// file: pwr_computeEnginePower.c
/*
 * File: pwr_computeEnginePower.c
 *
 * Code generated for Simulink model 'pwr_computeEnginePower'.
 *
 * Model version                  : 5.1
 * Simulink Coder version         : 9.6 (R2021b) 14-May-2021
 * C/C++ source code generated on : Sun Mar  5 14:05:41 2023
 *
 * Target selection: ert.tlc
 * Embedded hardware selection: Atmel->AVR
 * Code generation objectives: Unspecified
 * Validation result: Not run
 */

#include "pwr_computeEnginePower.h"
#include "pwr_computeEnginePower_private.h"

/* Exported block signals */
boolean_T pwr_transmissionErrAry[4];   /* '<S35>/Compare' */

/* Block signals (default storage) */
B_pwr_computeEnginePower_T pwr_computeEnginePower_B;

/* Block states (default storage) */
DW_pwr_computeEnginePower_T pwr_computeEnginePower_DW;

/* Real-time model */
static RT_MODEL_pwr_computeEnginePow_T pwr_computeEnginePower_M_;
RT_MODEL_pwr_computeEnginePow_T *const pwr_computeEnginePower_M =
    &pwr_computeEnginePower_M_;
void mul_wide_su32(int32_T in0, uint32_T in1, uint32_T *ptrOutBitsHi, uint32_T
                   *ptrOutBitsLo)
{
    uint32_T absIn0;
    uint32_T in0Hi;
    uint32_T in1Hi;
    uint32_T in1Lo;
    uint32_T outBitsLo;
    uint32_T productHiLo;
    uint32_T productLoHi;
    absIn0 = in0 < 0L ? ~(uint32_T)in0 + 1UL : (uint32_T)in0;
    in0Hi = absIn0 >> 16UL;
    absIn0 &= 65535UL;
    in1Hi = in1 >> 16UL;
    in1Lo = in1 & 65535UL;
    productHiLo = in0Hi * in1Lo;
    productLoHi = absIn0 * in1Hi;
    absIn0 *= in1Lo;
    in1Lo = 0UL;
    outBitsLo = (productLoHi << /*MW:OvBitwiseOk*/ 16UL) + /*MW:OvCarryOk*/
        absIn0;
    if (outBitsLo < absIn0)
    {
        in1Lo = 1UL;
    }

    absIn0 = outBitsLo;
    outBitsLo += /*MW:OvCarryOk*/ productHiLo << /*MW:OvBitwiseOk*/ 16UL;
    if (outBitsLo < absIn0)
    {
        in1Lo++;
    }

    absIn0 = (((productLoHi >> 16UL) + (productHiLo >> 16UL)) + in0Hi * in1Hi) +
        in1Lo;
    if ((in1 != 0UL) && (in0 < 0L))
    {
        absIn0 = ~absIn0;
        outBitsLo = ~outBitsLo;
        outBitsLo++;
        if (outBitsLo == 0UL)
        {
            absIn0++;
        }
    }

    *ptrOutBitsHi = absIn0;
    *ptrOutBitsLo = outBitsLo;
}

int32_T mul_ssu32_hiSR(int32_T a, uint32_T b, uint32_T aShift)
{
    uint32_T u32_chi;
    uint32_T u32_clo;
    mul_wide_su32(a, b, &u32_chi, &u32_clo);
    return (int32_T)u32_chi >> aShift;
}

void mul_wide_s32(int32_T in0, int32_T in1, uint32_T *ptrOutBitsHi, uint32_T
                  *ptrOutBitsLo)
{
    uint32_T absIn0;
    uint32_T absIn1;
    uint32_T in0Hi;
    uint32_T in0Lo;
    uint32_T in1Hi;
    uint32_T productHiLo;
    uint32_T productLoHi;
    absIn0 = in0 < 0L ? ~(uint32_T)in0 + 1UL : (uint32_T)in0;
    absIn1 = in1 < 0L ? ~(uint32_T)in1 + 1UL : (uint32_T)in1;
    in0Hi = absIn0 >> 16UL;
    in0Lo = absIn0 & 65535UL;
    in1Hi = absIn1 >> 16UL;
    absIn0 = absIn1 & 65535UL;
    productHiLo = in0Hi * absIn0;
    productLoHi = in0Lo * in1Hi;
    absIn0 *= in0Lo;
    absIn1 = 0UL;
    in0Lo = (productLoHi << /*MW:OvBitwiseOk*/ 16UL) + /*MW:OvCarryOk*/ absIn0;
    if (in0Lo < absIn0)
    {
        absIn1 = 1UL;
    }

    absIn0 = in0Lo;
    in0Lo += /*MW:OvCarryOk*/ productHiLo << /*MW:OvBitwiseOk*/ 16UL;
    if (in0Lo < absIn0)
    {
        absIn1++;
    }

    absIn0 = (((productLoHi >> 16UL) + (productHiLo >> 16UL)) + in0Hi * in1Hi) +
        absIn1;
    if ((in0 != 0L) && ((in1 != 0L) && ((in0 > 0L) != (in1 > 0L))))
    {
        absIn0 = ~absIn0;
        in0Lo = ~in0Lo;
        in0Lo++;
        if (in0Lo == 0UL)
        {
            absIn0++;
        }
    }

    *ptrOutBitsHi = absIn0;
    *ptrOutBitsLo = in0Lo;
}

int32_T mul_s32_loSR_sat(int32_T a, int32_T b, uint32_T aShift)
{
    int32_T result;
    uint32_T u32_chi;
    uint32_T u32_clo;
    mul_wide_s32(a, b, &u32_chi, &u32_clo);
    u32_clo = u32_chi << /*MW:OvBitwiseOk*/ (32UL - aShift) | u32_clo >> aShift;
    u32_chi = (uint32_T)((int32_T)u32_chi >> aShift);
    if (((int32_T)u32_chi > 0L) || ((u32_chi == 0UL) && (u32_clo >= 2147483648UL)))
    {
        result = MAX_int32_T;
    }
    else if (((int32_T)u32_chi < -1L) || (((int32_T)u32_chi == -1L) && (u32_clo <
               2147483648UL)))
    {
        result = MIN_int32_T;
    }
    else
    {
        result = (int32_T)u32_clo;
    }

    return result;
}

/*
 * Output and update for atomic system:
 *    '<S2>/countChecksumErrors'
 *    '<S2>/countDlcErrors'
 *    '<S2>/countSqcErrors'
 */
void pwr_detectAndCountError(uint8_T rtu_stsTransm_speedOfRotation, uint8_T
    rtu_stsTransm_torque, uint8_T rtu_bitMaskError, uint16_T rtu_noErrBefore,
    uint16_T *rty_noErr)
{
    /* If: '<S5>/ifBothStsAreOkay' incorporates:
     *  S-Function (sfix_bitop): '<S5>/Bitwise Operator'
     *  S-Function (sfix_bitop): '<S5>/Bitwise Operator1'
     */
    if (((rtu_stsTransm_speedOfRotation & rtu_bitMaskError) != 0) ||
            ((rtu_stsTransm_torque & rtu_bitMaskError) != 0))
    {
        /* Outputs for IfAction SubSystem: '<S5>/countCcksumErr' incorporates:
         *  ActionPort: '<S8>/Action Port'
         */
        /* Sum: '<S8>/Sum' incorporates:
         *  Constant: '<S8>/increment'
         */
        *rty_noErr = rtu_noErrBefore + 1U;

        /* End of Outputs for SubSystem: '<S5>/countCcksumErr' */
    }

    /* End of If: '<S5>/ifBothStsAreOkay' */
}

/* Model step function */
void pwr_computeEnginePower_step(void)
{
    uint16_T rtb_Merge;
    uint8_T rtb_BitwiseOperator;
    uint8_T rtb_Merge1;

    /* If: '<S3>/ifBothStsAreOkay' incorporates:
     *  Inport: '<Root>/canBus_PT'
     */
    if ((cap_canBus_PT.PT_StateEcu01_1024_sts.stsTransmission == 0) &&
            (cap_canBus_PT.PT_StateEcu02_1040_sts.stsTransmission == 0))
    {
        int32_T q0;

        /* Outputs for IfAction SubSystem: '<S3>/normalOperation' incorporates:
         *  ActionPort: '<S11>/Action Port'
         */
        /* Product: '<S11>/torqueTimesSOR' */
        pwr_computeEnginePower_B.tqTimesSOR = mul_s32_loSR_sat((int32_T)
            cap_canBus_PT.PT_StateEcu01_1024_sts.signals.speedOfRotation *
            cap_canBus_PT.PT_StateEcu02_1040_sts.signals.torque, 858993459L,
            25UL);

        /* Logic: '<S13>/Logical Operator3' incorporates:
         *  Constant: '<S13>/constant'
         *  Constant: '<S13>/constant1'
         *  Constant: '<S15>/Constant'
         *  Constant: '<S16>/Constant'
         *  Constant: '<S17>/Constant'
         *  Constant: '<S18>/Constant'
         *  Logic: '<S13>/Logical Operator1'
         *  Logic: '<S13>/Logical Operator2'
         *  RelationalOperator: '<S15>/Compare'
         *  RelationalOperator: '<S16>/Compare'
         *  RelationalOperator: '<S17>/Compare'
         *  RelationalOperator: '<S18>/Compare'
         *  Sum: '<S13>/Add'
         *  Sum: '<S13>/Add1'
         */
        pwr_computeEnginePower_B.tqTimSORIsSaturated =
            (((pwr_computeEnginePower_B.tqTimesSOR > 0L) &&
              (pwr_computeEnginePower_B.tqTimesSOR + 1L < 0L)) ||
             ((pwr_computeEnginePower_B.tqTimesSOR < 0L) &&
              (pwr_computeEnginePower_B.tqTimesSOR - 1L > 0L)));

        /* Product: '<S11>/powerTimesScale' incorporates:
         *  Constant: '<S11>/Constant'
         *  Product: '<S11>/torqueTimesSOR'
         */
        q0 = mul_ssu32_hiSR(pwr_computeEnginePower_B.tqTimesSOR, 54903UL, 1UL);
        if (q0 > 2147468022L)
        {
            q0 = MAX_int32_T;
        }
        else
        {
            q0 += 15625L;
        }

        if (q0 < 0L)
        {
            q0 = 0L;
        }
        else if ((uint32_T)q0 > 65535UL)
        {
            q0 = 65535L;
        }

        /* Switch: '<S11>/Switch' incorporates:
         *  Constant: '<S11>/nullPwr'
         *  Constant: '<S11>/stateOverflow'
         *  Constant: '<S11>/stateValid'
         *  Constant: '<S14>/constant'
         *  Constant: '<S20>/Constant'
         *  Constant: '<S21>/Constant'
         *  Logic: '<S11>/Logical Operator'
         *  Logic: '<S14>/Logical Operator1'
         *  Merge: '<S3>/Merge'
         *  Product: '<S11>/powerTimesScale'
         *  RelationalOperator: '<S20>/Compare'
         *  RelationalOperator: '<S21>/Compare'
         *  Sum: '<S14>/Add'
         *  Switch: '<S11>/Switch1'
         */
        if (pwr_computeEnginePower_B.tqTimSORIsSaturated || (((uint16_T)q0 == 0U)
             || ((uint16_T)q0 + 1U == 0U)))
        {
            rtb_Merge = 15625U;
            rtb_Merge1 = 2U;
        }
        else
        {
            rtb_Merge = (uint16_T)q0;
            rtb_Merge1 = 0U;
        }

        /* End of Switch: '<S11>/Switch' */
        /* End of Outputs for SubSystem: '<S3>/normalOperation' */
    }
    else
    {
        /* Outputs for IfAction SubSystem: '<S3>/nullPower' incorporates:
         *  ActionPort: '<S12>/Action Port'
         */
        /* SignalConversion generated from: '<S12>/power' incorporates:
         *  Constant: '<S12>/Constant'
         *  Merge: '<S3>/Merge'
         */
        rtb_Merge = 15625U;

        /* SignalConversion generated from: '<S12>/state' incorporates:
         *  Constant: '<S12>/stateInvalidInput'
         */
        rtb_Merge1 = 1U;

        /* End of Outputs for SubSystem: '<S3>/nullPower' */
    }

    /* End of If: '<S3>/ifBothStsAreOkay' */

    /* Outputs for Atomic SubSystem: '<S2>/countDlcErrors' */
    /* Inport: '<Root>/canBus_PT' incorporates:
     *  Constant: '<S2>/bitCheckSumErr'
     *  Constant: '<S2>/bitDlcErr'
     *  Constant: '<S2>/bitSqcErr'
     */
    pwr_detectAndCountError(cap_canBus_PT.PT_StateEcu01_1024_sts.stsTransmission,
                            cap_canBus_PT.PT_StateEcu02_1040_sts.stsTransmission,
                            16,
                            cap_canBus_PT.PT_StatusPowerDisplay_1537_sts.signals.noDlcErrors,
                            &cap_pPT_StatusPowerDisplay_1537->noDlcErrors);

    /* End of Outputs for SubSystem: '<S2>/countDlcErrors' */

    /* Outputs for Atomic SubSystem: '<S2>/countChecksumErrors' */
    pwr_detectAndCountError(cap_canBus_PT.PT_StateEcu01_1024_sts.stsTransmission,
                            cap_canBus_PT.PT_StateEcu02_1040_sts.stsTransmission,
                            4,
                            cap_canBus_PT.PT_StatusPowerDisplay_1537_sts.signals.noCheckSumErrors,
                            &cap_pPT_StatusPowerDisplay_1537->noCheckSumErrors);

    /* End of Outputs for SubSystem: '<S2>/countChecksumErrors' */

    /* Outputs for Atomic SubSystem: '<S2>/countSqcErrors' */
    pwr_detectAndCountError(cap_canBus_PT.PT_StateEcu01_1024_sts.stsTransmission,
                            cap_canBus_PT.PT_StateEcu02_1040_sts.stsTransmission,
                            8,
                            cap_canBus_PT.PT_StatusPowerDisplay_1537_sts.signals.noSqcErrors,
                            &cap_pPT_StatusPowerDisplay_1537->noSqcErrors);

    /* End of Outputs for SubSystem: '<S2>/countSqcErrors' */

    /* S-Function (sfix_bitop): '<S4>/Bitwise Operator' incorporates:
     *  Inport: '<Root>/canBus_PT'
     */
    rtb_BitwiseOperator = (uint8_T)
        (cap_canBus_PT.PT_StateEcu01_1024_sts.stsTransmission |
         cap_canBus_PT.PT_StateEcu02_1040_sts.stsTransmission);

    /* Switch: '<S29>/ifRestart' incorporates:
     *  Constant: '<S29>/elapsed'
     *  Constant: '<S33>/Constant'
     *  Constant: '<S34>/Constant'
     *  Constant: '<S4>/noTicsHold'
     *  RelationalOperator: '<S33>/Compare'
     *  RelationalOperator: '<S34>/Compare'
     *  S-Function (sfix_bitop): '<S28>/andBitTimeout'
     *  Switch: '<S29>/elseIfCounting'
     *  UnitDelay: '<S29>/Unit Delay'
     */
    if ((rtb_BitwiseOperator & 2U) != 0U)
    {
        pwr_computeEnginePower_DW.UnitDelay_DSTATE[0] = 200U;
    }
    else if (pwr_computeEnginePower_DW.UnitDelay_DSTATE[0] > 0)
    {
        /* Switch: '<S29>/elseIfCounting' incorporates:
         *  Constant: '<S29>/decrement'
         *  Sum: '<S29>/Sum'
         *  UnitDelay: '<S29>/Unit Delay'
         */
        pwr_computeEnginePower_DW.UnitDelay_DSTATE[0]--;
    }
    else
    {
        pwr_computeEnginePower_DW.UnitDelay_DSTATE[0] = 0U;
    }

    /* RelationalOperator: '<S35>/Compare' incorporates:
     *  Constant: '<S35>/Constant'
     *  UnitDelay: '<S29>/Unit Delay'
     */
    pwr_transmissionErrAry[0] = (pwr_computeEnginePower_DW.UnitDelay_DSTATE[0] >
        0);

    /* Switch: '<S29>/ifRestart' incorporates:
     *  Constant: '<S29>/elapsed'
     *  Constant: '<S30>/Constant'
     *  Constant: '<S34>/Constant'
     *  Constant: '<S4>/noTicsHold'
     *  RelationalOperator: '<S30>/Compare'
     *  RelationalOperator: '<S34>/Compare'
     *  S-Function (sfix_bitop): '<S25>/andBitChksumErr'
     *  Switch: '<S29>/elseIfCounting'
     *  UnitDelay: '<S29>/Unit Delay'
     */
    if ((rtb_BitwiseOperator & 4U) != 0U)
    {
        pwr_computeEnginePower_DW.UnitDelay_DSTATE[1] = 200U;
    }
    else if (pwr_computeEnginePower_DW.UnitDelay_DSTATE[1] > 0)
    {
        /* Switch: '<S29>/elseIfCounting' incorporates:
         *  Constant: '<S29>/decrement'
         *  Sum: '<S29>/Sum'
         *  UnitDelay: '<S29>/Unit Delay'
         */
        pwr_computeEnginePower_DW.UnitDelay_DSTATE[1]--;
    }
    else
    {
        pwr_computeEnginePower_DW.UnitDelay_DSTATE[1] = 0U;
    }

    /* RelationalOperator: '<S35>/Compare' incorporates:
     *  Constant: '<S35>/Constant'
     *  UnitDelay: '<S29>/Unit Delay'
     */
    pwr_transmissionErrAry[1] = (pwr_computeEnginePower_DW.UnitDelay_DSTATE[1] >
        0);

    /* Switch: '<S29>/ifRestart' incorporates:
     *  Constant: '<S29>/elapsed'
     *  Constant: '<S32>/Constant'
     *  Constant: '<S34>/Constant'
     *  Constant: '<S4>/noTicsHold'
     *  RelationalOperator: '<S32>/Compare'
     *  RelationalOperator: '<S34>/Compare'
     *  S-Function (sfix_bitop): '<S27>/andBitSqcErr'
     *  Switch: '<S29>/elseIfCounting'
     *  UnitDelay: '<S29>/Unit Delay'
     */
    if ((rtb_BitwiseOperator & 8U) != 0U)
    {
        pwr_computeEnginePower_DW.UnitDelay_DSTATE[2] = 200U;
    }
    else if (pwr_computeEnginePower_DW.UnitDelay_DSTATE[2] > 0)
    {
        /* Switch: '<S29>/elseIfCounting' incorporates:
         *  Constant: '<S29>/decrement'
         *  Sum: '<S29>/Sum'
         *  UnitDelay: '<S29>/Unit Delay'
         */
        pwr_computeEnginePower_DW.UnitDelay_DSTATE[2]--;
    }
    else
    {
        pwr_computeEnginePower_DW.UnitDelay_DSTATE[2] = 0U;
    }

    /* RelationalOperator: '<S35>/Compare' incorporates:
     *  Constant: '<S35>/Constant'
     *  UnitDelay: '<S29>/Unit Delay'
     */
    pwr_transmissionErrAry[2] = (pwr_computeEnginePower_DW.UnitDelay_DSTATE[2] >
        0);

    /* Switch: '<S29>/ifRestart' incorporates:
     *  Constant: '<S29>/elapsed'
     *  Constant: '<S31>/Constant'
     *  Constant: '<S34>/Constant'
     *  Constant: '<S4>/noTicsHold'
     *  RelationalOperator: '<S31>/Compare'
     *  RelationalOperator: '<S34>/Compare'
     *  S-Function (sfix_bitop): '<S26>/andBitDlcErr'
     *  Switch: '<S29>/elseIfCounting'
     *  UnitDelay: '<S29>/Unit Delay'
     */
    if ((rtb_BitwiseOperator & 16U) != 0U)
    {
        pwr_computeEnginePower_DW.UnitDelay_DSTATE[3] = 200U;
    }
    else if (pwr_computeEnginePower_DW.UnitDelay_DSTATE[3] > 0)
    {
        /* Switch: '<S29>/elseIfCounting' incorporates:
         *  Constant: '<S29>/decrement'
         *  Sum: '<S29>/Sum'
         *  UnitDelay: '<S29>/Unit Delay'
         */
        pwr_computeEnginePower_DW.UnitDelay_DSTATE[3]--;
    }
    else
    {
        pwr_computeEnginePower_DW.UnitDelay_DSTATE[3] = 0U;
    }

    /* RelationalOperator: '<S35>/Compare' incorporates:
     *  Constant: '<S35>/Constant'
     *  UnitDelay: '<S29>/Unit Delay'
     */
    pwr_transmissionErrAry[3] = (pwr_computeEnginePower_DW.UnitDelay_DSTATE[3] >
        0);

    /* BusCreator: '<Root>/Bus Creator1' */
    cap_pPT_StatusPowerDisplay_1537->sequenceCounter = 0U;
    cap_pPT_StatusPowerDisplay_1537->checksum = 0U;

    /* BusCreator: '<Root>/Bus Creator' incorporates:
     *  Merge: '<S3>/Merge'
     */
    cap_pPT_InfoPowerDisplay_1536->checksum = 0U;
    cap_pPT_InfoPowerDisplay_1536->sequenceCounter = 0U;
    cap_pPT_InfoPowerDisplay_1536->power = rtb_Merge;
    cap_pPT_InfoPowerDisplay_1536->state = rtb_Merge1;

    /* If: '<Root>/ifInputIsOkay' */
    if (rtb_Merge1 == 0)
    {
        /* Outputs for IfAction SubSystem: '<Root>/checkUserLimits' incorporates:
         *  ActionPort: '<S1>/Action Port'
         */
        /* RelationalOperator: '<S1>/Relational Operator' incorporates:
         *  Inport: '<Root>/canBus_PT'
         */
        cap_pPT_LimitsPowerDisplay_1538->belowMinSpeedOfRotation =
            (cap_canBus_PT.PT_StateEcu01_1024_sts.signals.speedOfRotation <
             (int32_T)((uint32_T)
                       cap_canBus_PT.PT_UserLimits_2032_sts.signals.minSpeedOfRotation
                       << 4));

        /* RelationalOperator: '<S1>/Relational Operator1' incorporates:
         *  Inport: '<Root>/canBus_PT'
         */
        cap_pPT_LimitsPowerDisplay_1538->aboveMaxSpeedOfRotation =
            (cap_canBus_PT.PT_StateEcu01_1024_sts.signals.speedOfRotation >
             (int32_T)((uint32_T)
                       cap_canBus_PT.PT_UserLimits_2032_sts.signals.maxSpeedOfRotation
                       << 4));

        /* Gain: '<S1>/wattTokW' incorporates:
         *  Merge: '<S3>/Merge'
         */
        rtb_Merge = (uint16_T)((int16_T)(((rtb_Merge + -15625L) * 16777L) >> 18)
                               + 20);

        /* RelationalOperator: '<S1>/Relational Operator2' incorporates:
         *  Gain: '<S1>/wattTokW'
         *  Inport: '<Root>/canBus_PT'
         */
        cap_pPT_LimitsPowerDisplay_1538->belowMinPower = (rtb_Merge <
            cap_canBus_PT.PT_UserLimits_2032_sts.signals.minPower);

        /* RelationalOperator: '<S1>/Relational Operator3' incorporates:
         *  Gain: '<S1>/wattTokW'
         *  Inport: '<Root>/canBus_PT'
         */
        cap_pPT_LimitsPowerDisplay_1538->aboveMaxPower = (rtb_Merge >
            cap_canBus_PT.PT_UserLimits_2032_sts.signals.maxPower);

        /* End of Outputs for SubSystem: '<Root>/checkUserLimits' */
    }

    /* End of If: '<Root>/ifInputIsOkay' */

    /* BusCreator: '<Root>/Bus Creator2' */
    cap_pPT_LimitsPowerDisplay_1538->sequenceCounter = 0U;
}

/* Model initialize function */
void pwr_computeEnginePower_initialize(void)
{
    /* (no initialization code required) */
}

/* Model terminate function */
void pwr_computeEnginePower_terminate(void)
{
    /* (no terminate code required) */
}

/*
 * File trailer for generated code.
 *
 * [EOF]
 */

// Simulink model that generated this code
simulink model "pwr_computeEnginePower"  (R2021b)
settings: Solver=FixedStepDiscrete  StartTime=0.0  StopTime=10.0  RelTol=1e-3
libraries: simulink x27

== system pwr_computeEnginePower ==
  note: The comparison of actual values of speed of rotation
      |  and power with the user specified limits is done only
      | if the received frames are valid. This information is
      | derived from the status of the computed power signal
  note: Checksum and sequence counter are not
      | computed by the APSW but by the code
      | integration layer (the upper CAN stack layer).
      | Unfortunately forces the use of bus objects
      | setting all signals of th bus, not only of
      | the required. We write dummy values here,
      | which will be overwritten by the CAN stack
  canBus_PT : Inport  OutDataTypeStr=Bus: cap_canBus_PT_t  BusOutputAsStruct=on
  Bus Creator : BusCreator  Inputs=4  OutDataTypeStr=Bus: cap_PT_InfoPowerDisplay_1536_t  NonVirtualBus=on
  Bus Creator1 : BusCreator  Inputs=5  OutDataTypeStr=Bus: cap_PT_StatusPowerDisplay_1537_t  NonVirtualBus=on
  Bus Creator2 : BusCreator  Inputs=5  OutDataTypeStr=Bus: cap_PT_LimitsPowerDisplay_1538_t  NonVirtualBus=on
  Bus Selector : BusSelector  OutputSignals=PT_StateEcu01_1024_sts.signals.speedOfRotation,PT_StateEcu01_1024_sts.stsTransmission,PT_StateEcu02_1040_sts.signals.torque,PT_StateEcu02_1040_sts.stsTransmission,PT_UserLimits_2032_sts.signals.minSpeedOfRotation,PT_UserLimits_2032_sts.signals.maxSpeedOfRotation,PT_UserLimits_2032_sts.signals.minPower,PT_UserLimits_2032_sts.signals.maxPower,PT_UserLimits_2032_sts.stsTransmission,PT_StatusPowerDisplay_1537_sts.signals.noDlcErrors,PT_StatusPowerDisplay_1537_sts.signals.noCheckSumErrors,PT_StatusPowerDisplay_1537_sts.signals.noSqcErrors
  Ground_{1,8..10,15} (5 alike) : Ground
  Terminator_8 : Terminator
  checkUserLimits : Subsystem  TreatAsAtomicUnit=on  RTWFcnName=pwr_detectAndCountError
  cntTransmissionErrs : Subsystem
  ifInputIsOkay : If  IfExpression=u1 == 0  ShowElse=off
  powerComputation : Subsystem
  transmissionErrs : Subsystem
  InfoPowerDisplay : Outport  OutDataTypeStr=Bus: cap_PT_InfoPowerDisplay_1536_t
  StatusPowerDisplay : Outport  Port=2  OutDataTypeStr=Bus: cap_PT_StatusPowerDisplay_1537_t
  LimitsPowerDisplay : Outport  Port=3  OutDataTypeStr=Bus: cap_PT_LimitsPowerDisplay_1538_t
  pwr_transmissionErrAry : Outport  Port=4
  wires:
  Bus Creator1/1 -> StatusPowerDisplay/1  "PT_StatusPowerDisplay_1537"
  Ground_15/1 -> Bus Creator/2  "sequenceCounter"
  Bus Selector/8 -> checkUserLimits/6(maxPwr)  "<maxPower>"
  Bus Selector/10 -> cntTransmissionErrs/3(noDlcErrBefore)  "<noDlcErrors>"
  Bus Selector/9 -> Terminator_8/1  "<stsTransmission>"
  Bus Selector/7 -> checkUserLimits/5(minPwr)  "<minPower>"
  powerComputation/1(power) -> Bus Creator/3, checkUserLimits/4(power)  "power"
  canBus_PT/1 -> Bus Selector/1  "canBus_PT"
  Bus Selector/6 -> checkUserLimits/3(maxSOR)  "<maxSpeedOfRotation>"
  powerComputation/2(state) -> Bus Creator/4, ifInputIsOkay/1  "state"
  cntTransmissionErrs/2(noChksumErrs) -> Bus Creator1/2
  ifInputIsOkay/1 -> checkUserLimits/Action
  Bus Selector/11 -> cntTransmissionErrs/4(noChksumErrBefore)  "<noCheckSumErrors>"
  Bus Selector/5 -> checkUserLimits/2(minSOR)  "<minSpeedOfRotation>"
  transmissionErrs/1(errVecHold) -> pwr_transmissionErrAry/1  "pwr_transmissionErrAry"
  Ground_1/1 -> Bus Creator/1  "checksum"
  checkUserLimits/4(aboveMaxPower) -> Bus Creator2/5  "aboveMaxPower"
  Bus Creator2/1 -> LimitsPowerDisplay/1  "PT_LimitsPowerDisplay_1538"
  cntTransmissionErrs/3(noSqcErrs) -> Bus Creator1/3
  Bus Selector/4 -> powerComputation/4(stsTransm_torque), cntTransmissionErrs/2(stsTransm_torque1), transmissionErrs/2(stsTransm_torque)  "<stsTransmission>"
  checkUserLimits/3(belowMinPower) -> Bus Creator2/4  "belowMinPower"
  Ground_9/1 -> Bus Creator1/5  "checksum"
  Bus Selector/1 -> powerComputation/1(speedOfRotation), checkUserLimits/1(speedOfRotation)  "<speedOfRotation>"
  checkUserLimits/2(aboveMaxSpeedOfRotation) -> Bus Creator2/3  "aboveMaxSpeedOfRotation"
  Bus Selector/3 -> powerComputation/3(torque)  "<torque>"
  cntTransmissionErrs/1(noDlcErrs) -> Bus Creator1/1
  Bus Selector/12 -> cntTransmissionErrs/5(noSqcErrBefore)  "<noSqcErrors>"
  Bus Selector/2 -> powerComputation/2(stsTransm_speedOfRotation), cntTransmissionErrs/1(stsTransm_speedOfRotation), transmissionErrs/1(stsTransm_speedOfRotation)  "<stsTransmission>"
  checkUserLimits/1(belowMinSpeedOfRotation) -> Bus Creator2/2  "belowMinSpeedOfRotation"
  Bus Creator/1 -> InfoPowerDisplay/1  "PT_InfoPowerDisplay_1536"
  Ground_8/1 -> Bus Creator1/4  "sequenceCounter"
  Ground_10/1 -> Bus Creator2/1  "sequenceCounter"

== system pwr_computeEnginePower/checkUserLimits ==
  note: The input signals power limit
      | have the unit kW, whereas all other
      | power computation is done in W.
      | This is not part of the Embedded
      | Coder's scaling information and is
      | hence not considered by the code
      | generation. We need to perform
      | this kind of rescaling by an explicit
      | multiplication operation
  note: The rescaling required to implement
      | the comparisons introduce rounding
      | off errors, which make the limits check
      | not perfectly hit the boundaries. This
      | holds for SOR and power
  speedOfRotation : Inport
  minSOR : Inport  Port=2
  maxSOR : Inport  Port=3
  power : Inport  Port=4
  minPwr : Inport  Port=5
  maxPwr : Inport  Port=6
  Action Port : ActionPort  PropagateVarSize=During execution  ActionPortLabel=if(u1 == 0)
  Relational Operator : RelationalOperator  Operator=<  OutDataTypeStr=boolean  RndMeth=Nearest
  Relational Operator1 : RelationalOperator  Operator=>  OutDataTypeStr=boolean  RndMeth=Nearest
  Relational Operator2 : RelationalOperator  Operator=<  OutDataTypeStr=boolean  RndMeth=Nearest
  Relational Operator3 : RelationalOperator  Operator=>  OutDataTypeStr=boolean  RndMeth=Nearest
  wattTokW : Gain  Gain=0.001  OutDataTypeStr=fixdt(0,16,2^-1,-10)
  belowMinSpeedOfRotation : Outport
  aboveMaxSpeedOfRotation : Outport  Port=2
  belowMinPower : Outport  Port=3
  aboveMaxPower : Outport  Port=4
  wires:
  speedOfRotation/1 -> Relational Operator/1, Relational Operator1/1
  minSOR/1 -> Relational Operator/2
  Relational Operator/1 -> belowMinSpeedOfRotation/1
  maxSOR/1 -> Relational Operator1/2
  Relational Operator1/1 -> aboveMaxSpeedOfRotation/1
  power/1 -> wattTokW/1
  minPwr/1 -> Relational Operator2/2
  Relational Operator2/1 -> belowMinPower/1
  maxPwr/1 -> Relational Operator3/2
  Relational Operator3/1 -> aboveMaxPower/1
  wattTokW/1 -> Relational Operator2/1, Relational Operator3/1

== system pwr_computeEnginePower/cntTransmissionErrs ==
  stsTransm_speedOfRotation : Inport
  stsTransm_torque1 : Inport  Port=2
  noDlcErrBefore : Inport  Port=3
  noChksumErrBefore : Inport  Port=4
  noSqcErrBefore : Inport  Port=5
  bitCheckSumErr : Constant  Value=4  OutDataTypeStr=uint8
  bitDlcErr : Constant  Value=16  OutDataTypeStr=uint8
  bitSqcErr : Constant  Value=8  OutDataTypeStr=uint8
  countChecksumErrors : Subsystem  TreatAsAtomicUnit=on  RTWFcnName=pwr_detectAndCountError
  countDlcErrors : Subsystem  TreatAsAtomicUnit=on  RTWFcnName=pwr_detectAndCountError
  countSqcErrors : Subsystem  TreatAsAtomicUnit=on  RTWFcnName=pwr_detectAndCountError
  noDlcErrs : Outport
  noChksumErrs : Outport  Port=2
  noSqcErrs : Outport  Port=3
  wires:
  bitDlcErr/1 -> countDlcErrors/3(bitMaskError)
  bitCheckSumErr/1 -> countChecksumErrors/3(bitMaskError)
  bitSqcErr/1 -> countSqcErrors/3(bitMaskError)
  stsTransm_speedOfRotation/1 -> countDlcErrors/1(stsTransm_speedOfRotation), countChecksumErrors/1(stsTransm_speedOfRotation), countSqcErrors/1(stsTransm_speedOfRotation)
  stsTransm_torque1/1 -> countDlcErrors/2(stsTransm_torque), countChecksumErrors/2(stsTransm_torque), countSqcErrors/2(stsTransm_torque)
  countDlcErrors/1(noErr) -> noDlcErrs/1  "noDlcErrors"
  noDlcErrBefore/1 -> countDlcErrors/4(noErrBefore)
  countChecksumErrors/1(noErr) -> noChksumErrs/1  "noCheckSumErrors"
  noChksumErrBefore/1 -> countChecksumErrors/4(noErrBefore)
  countSqcErrors/1(noErr) -> noSqcErrs/1  "noSqcErrors"
  noSqcErrBefore/1 -> countSqcErrors/4(noErrBefore)

== system pwr_computeEnginePower/powerComputation ==
  speedOfRotation : Inport
  stsTransm_speedOfRotation : Inport  Port=2
  torque : Inport  Port=3
  stsTransm_torque : Inport  Port=4
  Merge : Merge
  Merge1 : Merge
  ifBothStsAreOkay : If  NumInputs=2  IfExpression="u1 == 0  &  u2 == 0"
  normalOperation : Subsystem  TreatAsAtomicUnit=on
  nullPower : Subsystem  TreatAsAtomicUnit=on
  power : Outport
  state : Outport  Port=2
  wires:
  speedOfRotation/1 -> normalOperation/1(speedOfRotation)
  stsTransm_speedOfRotation/1 -> ifBothStsAreOkay/1
  stsTransm_torque/1 -> ifBothStsAreOkay/2
  ifBothStsAreOkay/1 -> normalOperation/Action
  torque/1 -> normalOperation/2(torque)
  ifBothStsAreOkay/2 -> nullPower/Action
  normalOperation/1(power) -> Merge/1
  nullPower/1(power) -> Merge/2
  normalOperation/2(state) -> Merge1/1
  nullPower/2(state) -> Merge1/2
  Merge/1 -> power/1
  Merge1/1 -> state/1

== system pwr_computeEnginePower/transmissionErrs ==
  stsTransm_speedOfRotation : Inport
  stsTransm_torque : Inport  Port=2
  Bitwise Operator : simulink/Logic and Bit Operations/Bitwise Operator  logicop=OR  UseBitMask=off  NumInputPorts=2  BitMask=bin2dec('11011001')  BitMaskRealWorld=Stored Integer
  Data Type Scaling Strip : simulink/Signal Attributes/Data Type Scaling Strip
  Data Type Scaling Strip1 : simulink/Signal Attributes/Data Type Scaling Strip
  Mux : Mux
  filterBitChksumErr : Subsystem
  filterBitDlcErr : Subsystem
  filterBitSqcErr : Subsystem
  filterBitTimeout : Subsystem
  hold : Subsystem
  noTicsHold : Constant  Value=200  OutDataTypeStr=uint8
  errVecHold : Outport
  wires:
  stsTransm_speedOfRotation/1 -> Data Type Scaling Strip/1
  stsTransm_torque/1 -> Data Type Scaling Strip1/1
  Data Type Scaling Strip/1 -> Bitwise Operator/1
  Mux/1 -> hold/1(boolVec)  "errVec"
  Data Type Scaling Strip1/1 -> Bitwise Operator/2
  Bitwise Operator/1 -> filterBitSqcErr/1(bitVec), filterBitDlcErr/1(bitVec), filterBitChksumErr/1(bitVec), filterBitTimeout/1(bitVec)
  filterBitChksumErr/1(isChksumErr) -> Mux/2
  filterBitSqcErr/1(isSqcErr) -> Mux/3
  filterBitDlcErr/1(Out1) -> Mux/4
  filterBitTimeout/1(isTimeout) -> Mux/1
  hold/1(boolVecHold) -> errVecHold/1
  noTicsHold/1 -> hold/2(noTicsHold)

== system pwr_computeEnginePower/cntTransmissionErrs/countChecksumErrors ==
  stsTransm_speedOfRotation : Inport
  stsTransm_torque : Inport  Port=2
  bitMaskError : Inport  Port=3
  noErrBefore : Inport  Port=4
  Bitwise Operator : simulink/Logic and Bit Operations/Bitwise Operator  logicop=AND  UseBitMask=off  NumInputPorts=2  BitMask=bin2dec('11011001')  BitMaskRealWorld=Stored Integer
  Bitwise Operator1 : simulink/Logic and Bit Operations/Bitwise Operator  logicop=AND  UseBitMask=off  NumInputPorts=2  BitMask=bin2dec('11011001')  BitMaskRealWorld=Stored Integer
  countCcksumErr : Subsystem  TreatAsAtomicUnit=on
  ifBothStsAreOkay : If  NumInputs=2  IfExpression="u1 ~= 0  |  u2 ~= 0"  ShowElse=off
  noErr : Outport
  wires:
  ifBothStsAreOkay/1 -> countCcksumErr/Action
  stsTransm_torque/1 -> Bitwise Operator1/1
  stsTransm_speedOfRotation/1 -> Bitwise Operator/1
  noErrBefore/1 -> countCcksumErr/1(noErrBefore)
  countCcksumErr/1(noErr) -> noErr/1
  bitMaskError/1 -> Bitwise Operator/2, Bitwise Operator1/2
  Bitwise Operator/1 -> ifBothStsAreOkay/1
  Bitwise Operator1/1 -> ifBothStsAreOkay/2

== system pwr_computeEnginePower/cntTransmissionErrs/countDlcErrors ==
  stsTransm_speedOfRotation : Inport
  stsTransm_torque : Inport  Port=2
  bitMaskError : Inport  Port=3
  noErrBefore : Inport  Port=4
  Bitwise Operator : simulink/Logic and Bit Operations/Bitwise Operator  logicop=AND  UseBitMask=off  NumInputPorts=2  BitMask=bin2dec('11011001')  BitMaskRealWorld=Stored Integer
  Bitwise Operator1 : simulink/Logic and Bit Operations/Bitwise Operator  logicop=AND  UseBitMask=off  NumInputPorts=2  BitMask=bin2dec('11011001')  BitMaskRealWorld=Stored Integer
  countCcksumErr : Subsystem  TreatAsAtomicUnit=on
  ifBothStsAreOkay : If  NumInputs=2  IfExpression="u1 ~= 0  |  u2 ~= 0"  ShowElse=off
  noErr : Outport
  wires:
  ifBothStsAreOkay/1 -> countCcksumErr/Action
  stsTransm_torque/1 -> Bitwise Operator1/1
  stsTransm_speedOfRotation/1 -> Bitwise Operator/1
  noErrBefore/1 -> countCcksumErr/1(noErrBefore)
  countCcksumErr/1(noErr) -> noErr/1
  bitMaskError/1 -> Bitwise Operator/2, Bitwise Operator1/2
  Bitwise Operator/1 -> ifBothStsAreOkay/1
  Bitwise Operator1/1 -> ifBothStsAreOkay/2

== system pwr_computeEnginePower/cntTransmissionErrs/countSqcErrors ==
  stsTransm_speedOfRotation : Inport
  stsTransm_torque : Inport  Port=2
  bitMaskError : Inport  Port=3
  noErrBefore : Inport  Port=4
  Bitwise Operator : simulink/Logic and Bit Operations/Bitwise Operator  logicop=AND  UseBitMask=off  NumInputPorts=2  BitMask=bin2dec('11011001')  BitMaskRealWorld=Stored Integer
  Bitwise Operator1 : simulink/Logic and Bit Operations/Bitwise Operator  logicop=AND  UseBitMask=off  NumInputPorts=2  BitMask=bin2dec('11011001')  BitMaskRealWorld=Stored Integer
  countCcksumErr : Subsystem  TreatAsAtomicUnit=on
  ifBothStsAreOkay : If  NumInputs=2  IfExpression="u1 ~= 0  |  u2 ~= 0"  ShowElse=off
  noErr : Outport
  wires:
  Bitwise Operator1/1 -> ifBothStsAreOkay/2
  Bitwise Operator/1 -> ifBothStsAreOkay/1
  bitMaskError/1 -> Bitwise Operator1/2, Bitwise Operator/2
  countCcksumErr/1(noErr) -> noErr/1
  noErrBefore/1 -> countCcksumErr/1(noErrBefore)
  stsTransm_speedOfRotation/1 -> Bitwise Operator/1
  stsTransm_torque/1 -> Bitwise Operator1/1
  ifBothStsAreOkay/1 -> countCcksumErr/Action

== system pwr_computeEnginePower/powerComputation/normalOperation ==
  note: Caution, with MATLAB 2019b, the behavior of the multiplication seems
      | to have changed (with respect to M2009b, which the model was
      | originally made for). The product block no longer saturates to the
      | implementation limits and the overflow detection doesn't work any
      | longer as expected.
  note: The concept of the out-of-range detection is to rely on the integer saturation
      | of the Embedded Coder. Here, it is applied to the second product. It'll limit
      | the output to the maximum integer range of the output but not to the specified
      | signal range of the output.
      |   All too large values will be limited to the integer maximum, which is above
      | the permitted signal range. A <= operation is appropriate to filter all of these
      | bad values.
      |   All too large negative values will be limited to the lowerst integer value, which
      | is the minimum permitted signal value at the same time. It's a binary zero. We
      | can't distinguish between a good but extreme value or a limited one if we see
      | the binary zero. This is ignored; binary zero is always considered a bad value.
      | Our logic effectively decreases the output signal range by one unit.
      |   A perfect out-of-range detection is nearly impossible in fixed point
      | computation since it requires some insight into the product operation. This
      | insight does the EC have during code generation but we don't have it on the
      | Simulink level.
      |  The best compromise would be the rule to never include the largest and
      | lowest integer values in the permitted signal range - then a safe detection
      | becomes possible in the way we present it here
  speedOfRotation : Inport
  torque : Inport  Port=2
  Action Port : ActionPort  PropagateVarSize=During execution  ActionPortLabel="if(u1 == 0  &  u2 == 0)"
  Constant : Constant  Value=2*3.1415927/60  OutDataTypeStr=fixdt(0,16,19)
  Logical Operator : Logic  Operator=OR  AllPortsSameDT=off  OutDataTypeStr=boolean
  Switch : Switch  Criteria=u2 ~= 0  OutDataTypeStr=Inherit: Inherit via back propagation
  Switch1 : Switch  Criteria=u2 ~= 0  OutDataTypeStr=Inherit: Inherit via back propagation
  isSaturated : Subsystem
  isSaturated1 : Subsystem
  nullPwr : Constant  Value=0  OutDataTypeStr=Inherit: Inherit via back propagation
  powerTimesScale : Product  OutDataTypeStr=fixdt(0,16,2^5,-500000)  RndMeth=Simplest  SaturateOnIntegerOverflow=on
  stateOverflow : Constant  Value=2  OutDataTypeStr=uint8
  stateValid : Constant  Value=0  OutDataTypeStr=uint8
  torqueTimesSOR : Product  OutMin=6553.5*(-500)  OutMax=6553.5*500  OutDataTypeStr=fixdt(1,32,9)  RndMeth=Simplest  SaturateOnIntegerOverflow=on
  power : Outport  InitialOutput=0
  state : Outport  Port=2  InitialOutput=1
  wires:
  speedOfRotation/1 -> torqueTimesSOR/1
  torque/1 -> torqueTimesSOR/2
  Constant/1 -> powerTimesScale/2
  powerTimesScale/1 -> isSaturated1/1(unsignedInt), Switch/3
  Switch/1 -> power/1
  Logical Operator/1 -> Switch1/2, Switch/2  "pwrIsOutOfRange"
  stateOverflow/1 -> Switch1/1
  stateValid/1 -> Switch1/3
  Switch1/1 -> state/1
  torqueTimesSOR/1 -> powerTimesScale/1, isSaturated/1(signedInt)  "tqTimesSOR"
  isSaturated/1(isAtLimit) -> Logical Operator/1  "tqTimSORIsSaturated"
  isSaturated1/1(isAtLimit) -> Logical Operator/2  "timFacIsSaturated"
  nullPwr/1 -> Switch/1

== system pwr_computeEnginePower/powerComputation/nullPower ==
  Action Port : ActionPort  PropagateVarSize=During execution  ActionPortLabel=else
  Constant : Constant  Value=0  OutDataTypeStr=Inherit: Inherit via back propagation
  stateInvalidInput : Constant  OutDataTypeStr=uint8
  power : Outport  InitialOutput=0
  state : Outport  Port=2  InitialOutput=1
  wires:
  Constant/1 -> power/1
  stateInvalidInput/1 -> state/1

== system pwr_computeEnginePower/transmissionErrs/filterBitChksumErr ==
  bitVec : Inport
  Compare To Zero : simulink/Logic and Bit Operations/Compare To Zero  relop=~=  OutDataTypeStr=boolean  ZeroCross=off
  andBitChksumErr : simulink/Logic and Bit Operations/Bitwise Operator  logicop=AND  UseBitMask=on  BitMask=4  BitMaskRealWorld=Stored Integer
  isChksumErr : Outport
  wires:
  bitVec/1 -> andBitChksumErr/1
  andBitChksumErr/1 -> Compare To Zero/1
  Compare To Zero/1 -> isChksumErr/1  "isChksumErr"

== system pwr_computeEnginePower/transmissionErrs/filterBitDlcErr ==
  bitVec : Inport
  Compare To Zero : simulink/Logic and Bit Operations/Compare To Zero  relop=~=  OutDataTypeStr=boolean  ZeroCross=off
  andBitDlcErr : simulink/Logic and Bit Operations/Bitwise Operator  logicop=AND  UseBitMask=on  BitMask=16  BitMaskRealWorld=Stored Integer
  Out1 : Outport
  wires:
  bitVec/1 -> andBitDlcErr/1
  andBitDlcErr/1 -> Compare To Zero/1
  Compare To Zero/1 -> Out1/1  "isDlcErr"

== system pwr_computeEnginePower/transmissionErrs/filterBitSqcErr ==
  note: isSqcErr
  bitVec : Inport
  Compare To Zero : simulink/Logic and Bit Operations/Compare To Zero  relop=~=  OutDataTypeStr=boolean  ZeroCross=off
  andBitSqcErr : simulink/Logic and Bit Operations/Bitwise Operator  logicop=AND  UseBitMask=on  BitMask=8  BitMaskRealWorld=Stored Integer
  isSqcErr : Outport
  wires:
  bitVec/1 -> andBitSqcErr/1
  andBitSqcErr/1 -> Compare To Zero/1
  Compare To Zero/1 -> isSqcErr/1

== system pwr_computeEnginePower/transmissionErrs/filterBitTimeout ==
  bitVec : Inport
  Compare To Zero : simulink/Logic and Bit Operations/Compare To Zero  relop=~=  OutDataTypeStr=boolean  ZeroCross=off
  andBitTimeout : simulink/Logic and Bit Operations/Bitwise Operator  logicop=AND  UseBitMask=on  BitMask=2  BitMaskRealWorld=Stored Integer
  isTimeout : Outport
  wires:
  andBitTimeout/1 -> Compare To Zero/1  "errTimeout"
  bitVec/1 -> andBitTimeout/1
  Compare To Zero/1 -> isTimeout/1  "isTimeout"

== system pwr_computeEnginePower/transmissionErrs/hold ==
  boolVec : Inport
  noTicsHold : Inport  Port=2
  Compare To Zero : simulink/Logic and Bit Operations/Compare To Zero  relop=>  OutDataTypeStr=boolean  ZeroCross=off
  Compare To Zero1 : simulink/Logic and Bit Operations/Compare To Zero  relop=>  OutDataTypeStr=boolean  ZeroCross=off
  Sum : Sum  Inputs=|-+
  Unit Delay : UnitDelay  SampleTime=-1
  decrement : Constant  OutDataTypeStr=uint8
  elapsed : Constant  Value=0  OutDataTypeStr=uint8
  elseIfCounting : Switch  Criteria=u2 ~= 0
  ifRestart : Switch  Criteria=u2 ~= 0
  boolVecHold : Outport
  wires:
  noTicsHold/1 -> ifRestart/1
  Unit Delay/1 -> Sum/2, Compare To Zero/1
  Sum/1 -> elseIfCounting/1
  decrement/1 -> Sum/1
  elapsed/1 -> elseIfCounting/3
  ifRestart/1 -> Unit Delay/1, Compare To Zero1/1  "cntHold"
  elseIfCounting/1 -> ifRestart/3
  Compare To Zero/1 -> elseIfCounting/2
  Compare To Zero1/1 -> boolVecHold/1  "boolVecHold"
  boolVec/1 -> ifRestart/2

== system pwr_computeEnginePower/cntTransmissionErrs/countChecksumErrors/countCcksumErr ==
  noErrBefore : Inport
  Action Port : ActionPort  PropagateVarSize=During execution  ActionPortLabel="if(u1 ~= 0  |  u2 ~= 0)"
  Sum : Sum  Inputs=|++
  increment : Constant  OutDataTypeStr=uint8
  noErr : Outport
  wires:
  noErrBefore/1 -> Sum/1
  Sum/1 -> noErr/1  "noChecksumErrors"
  increment/1 -> Sum/2

== system pwr_computeEnginePower/cntTransmissionErrs/countDlcErrors/countCcksumErr ==
  noErrBefore : Inport
  Action Port : ActionPort  PropagateVarSize=During execution  ActionPortLabel="if(u1 ~= 0  |  u2 ~= 0)"
  Sum : Sum  Inputs=|++
  increment : Constant  OutDataTypeStr=uint8
  noErr : Outport
  wires:
  noErrBefore/1 -> Sum/1
  Sum/1 -> noErr/1  "noDlcErrors"
  increment/1 -> Sum/2

== system pwr_computeEnginePower/cntTransmissionErrs/countSqcErrors/countCcksumErr ==
  noErrBefore : Inport
  Action Port : ActionPort  PropagateVarSize=During execution  ActionPortLabel="if(u1 ~= 0  |  u2 ~= 0)"
  Sum : Sum  Inputs=|++
  increment : Constant  OutDataTypeStr=uint8
  noErr : Outport
  wires:
  increment/1 -> Sum/2
  Sum/1 -> noErr/1  "noSqcErrors"
  noErrBefore/1 -> Sum/1

== system pwr_computeEnginePower/powerComputation/normalOperation/isSaturated ==
  note: The concept of the out-of-range detection is to rely on the integer saturation
      | of the Embedded Coder. It is applied to the product at the beginning. It'll limit
      | the output to the maximum integer range of the output but not to the specified
      | signal range of the output.
      |   All too large values will be limited to the integer maximum, which is above
      | the permitted signal range. A <= operation is appropriate to filter all of these
      | bad values.
      |   All too large negative values will be limited to the lowerst integer value, which
      | is the minimum permitted signal value at the same time. It's a binary zero. We
      | can't distinguish between a good but extreme value or a limited one if we see
      | the binary zero. This is ignored; binary zero is always considered a bad value.
      | Our logic effectively decreases the output signal range by one unit.
      |   A perfect out-of-range detection is nearly impossible in fixed point
      | computation since it requires some insight into the product operation. This
      | insight does the EC have during code generation but we don't have it on the
      | Simulink level.
      |  The best compromise would be the rule to never include the largest and
      | lowest integer values in the permitted signal range - then a safe detection
      | becomes possible in the way we present it here
  signedInt : Inport
  Add : Sum  OutDataTypeStr=Inherit: Same as accumulator  RndMeth=Simplest
  Add1 : Sum  Inputs=+-  OutDataTypeStr=Inherit: Same as accumulator  RndMeth=Simplest
  Compare To Zero : simulink/Logic and Bit Operations/Compare To Zero  relop=<  OutDataTypeStr=boolean  ZeroCross=off
  Compare To Zero1 : simulink/Logic and Bit Operations/Compare To Zero  relop=>  OutDataTypeStr=boolean  ZeroCross=off
  Compare To Zero2 : simulink/Logic and Bit Operations/Compare To Zero  relop=<  OutDataTypeStr=boolean  ZeroCross=off
  Compare To Zero3 : simulink/Logic and Bit Operations/Compare To Zero  relop=>  OutDataTypeStr=boolean  ZeroCross=off
  Logical Operator1 : Logic  AllPortsSameDT=off  OutDataTypeStr=boolean
  Logical Operator2 : Logic  AllPortsSameDT=off  OutDataTypeStr=boolean
  Logical Operator3 : Logic  Operator=OR  AllPortsSameDT=off  OutDataTypeStr=boolean
  constant : Constant  OutDataTypeStr=Inherit: Inherit via back propagation
  constant1 : Constant  OutDataTypeStr=Inherit: Inherit via back propagation
  makeRawInteger : simulink/Signal Attributes/Data Type Scaling Strip
  isAtLimit : Outport
  wires:
  constant/1 -> Add/2
  signedInt/1 -> makeRawInteger/1
  Add/1 -> Compare To Zero/1
  constant1/1 -> Add1/2
  Add1/1 -> Compare To Zero1/1
  Compare To Zero2/1 -> Logical Operator2/1
  Compare To Zero1/1 -> Logical Operator2/2
  Compare To Zero3/1 -> Logical Operator1/1
  Compare To Zero/1 -> Logical Operator1/2
  Logical Operator1/1 -> Logical Operator3/1
  Logical Operator2/1 -> Logical Operator3/2
  Logical Operator3/1 -> isAtLimit/1
  makeRawInteger/1 -> Add/1, Add1/1, Compare To Zero2/1, Compare To Zero3/1

== system pwr_computeEnginePower/powerComputation/normalOperation/isSaturated1 ==
  note: The concept of the out-of-range detection is to rely on the integer saturation
      | of the Embedded Coder. It is applied to the product at the beginning. It'll limit
      | the output to the maximum integer range of the output but not to the specified
      | signal range of the output.
      |   All too large values will be limited to the integer maximum, which is above
      | the permitted signal range. A <= operation is appropriate to filter all of these
      | bad values.
      |   All too large negative values will be limited to the lowerst integer value, which
      | is the minimum permitted signal value at the same time. It's a binary zero. We
      | can't distinguish between a good but extreme value or a limited one if we see
      | the binary zero. This is ignored; binary zero is always considered a bad value.
      | Our logic effectively decreases the output signal range by one unit.
      |   A perfect out-of-range detection is nearly impossible in fixed point
      | computation since it requires some insight into the product operation. This
      | insight does the EC have during code generation but we don't have it on the
      | Simulink level.
      |  The best compromise would be the rule to never include the largest and
      | lowest integer values in the permitted signal range - then a safe detection
      | becomes possible in the way we present it here
  unsignedInt : Inport
  Add : Sum  OutDataTypeStr=Inherit: Same as accumulator  RndMeth=Simplest
  Compare To Zero : simulink/Logic and Bit Operations/Compare To Zero  relop===  OutDataTypeStr=boolean  ZeroCross=off
  Compare To Zero3 : simulink/Logic and Bit Operations/Compare To Zero  relop===  OutDataTypeStr=boolean  ZeroCross=off
  Logical Operator1 : Logic  Operator=OR  AllPortsSameDT=off  OutDataTypeStr=boolean
  constant : Constant  OutDataTypeStr=Inherit: Inherit via back propagation
  makeRawInteger : simulink/Signal Attributes/Data Type Scaling Strip
  isAtLimit : Outport
  wires:
  makeRawInteger/1 -> Compare To Zero3/1, Add/1
  Logical Operator1/1 -> isAtLimit/1
  Compare To Zero/1 -> Logical Operator1/2
  Compare To Zero3/1 -> Logical Operator1/1
  Add/1 -> Compare To Zero/1
  unsignedInt/1 -> makeRawInteger/1
  constant/1 -> Add/2
